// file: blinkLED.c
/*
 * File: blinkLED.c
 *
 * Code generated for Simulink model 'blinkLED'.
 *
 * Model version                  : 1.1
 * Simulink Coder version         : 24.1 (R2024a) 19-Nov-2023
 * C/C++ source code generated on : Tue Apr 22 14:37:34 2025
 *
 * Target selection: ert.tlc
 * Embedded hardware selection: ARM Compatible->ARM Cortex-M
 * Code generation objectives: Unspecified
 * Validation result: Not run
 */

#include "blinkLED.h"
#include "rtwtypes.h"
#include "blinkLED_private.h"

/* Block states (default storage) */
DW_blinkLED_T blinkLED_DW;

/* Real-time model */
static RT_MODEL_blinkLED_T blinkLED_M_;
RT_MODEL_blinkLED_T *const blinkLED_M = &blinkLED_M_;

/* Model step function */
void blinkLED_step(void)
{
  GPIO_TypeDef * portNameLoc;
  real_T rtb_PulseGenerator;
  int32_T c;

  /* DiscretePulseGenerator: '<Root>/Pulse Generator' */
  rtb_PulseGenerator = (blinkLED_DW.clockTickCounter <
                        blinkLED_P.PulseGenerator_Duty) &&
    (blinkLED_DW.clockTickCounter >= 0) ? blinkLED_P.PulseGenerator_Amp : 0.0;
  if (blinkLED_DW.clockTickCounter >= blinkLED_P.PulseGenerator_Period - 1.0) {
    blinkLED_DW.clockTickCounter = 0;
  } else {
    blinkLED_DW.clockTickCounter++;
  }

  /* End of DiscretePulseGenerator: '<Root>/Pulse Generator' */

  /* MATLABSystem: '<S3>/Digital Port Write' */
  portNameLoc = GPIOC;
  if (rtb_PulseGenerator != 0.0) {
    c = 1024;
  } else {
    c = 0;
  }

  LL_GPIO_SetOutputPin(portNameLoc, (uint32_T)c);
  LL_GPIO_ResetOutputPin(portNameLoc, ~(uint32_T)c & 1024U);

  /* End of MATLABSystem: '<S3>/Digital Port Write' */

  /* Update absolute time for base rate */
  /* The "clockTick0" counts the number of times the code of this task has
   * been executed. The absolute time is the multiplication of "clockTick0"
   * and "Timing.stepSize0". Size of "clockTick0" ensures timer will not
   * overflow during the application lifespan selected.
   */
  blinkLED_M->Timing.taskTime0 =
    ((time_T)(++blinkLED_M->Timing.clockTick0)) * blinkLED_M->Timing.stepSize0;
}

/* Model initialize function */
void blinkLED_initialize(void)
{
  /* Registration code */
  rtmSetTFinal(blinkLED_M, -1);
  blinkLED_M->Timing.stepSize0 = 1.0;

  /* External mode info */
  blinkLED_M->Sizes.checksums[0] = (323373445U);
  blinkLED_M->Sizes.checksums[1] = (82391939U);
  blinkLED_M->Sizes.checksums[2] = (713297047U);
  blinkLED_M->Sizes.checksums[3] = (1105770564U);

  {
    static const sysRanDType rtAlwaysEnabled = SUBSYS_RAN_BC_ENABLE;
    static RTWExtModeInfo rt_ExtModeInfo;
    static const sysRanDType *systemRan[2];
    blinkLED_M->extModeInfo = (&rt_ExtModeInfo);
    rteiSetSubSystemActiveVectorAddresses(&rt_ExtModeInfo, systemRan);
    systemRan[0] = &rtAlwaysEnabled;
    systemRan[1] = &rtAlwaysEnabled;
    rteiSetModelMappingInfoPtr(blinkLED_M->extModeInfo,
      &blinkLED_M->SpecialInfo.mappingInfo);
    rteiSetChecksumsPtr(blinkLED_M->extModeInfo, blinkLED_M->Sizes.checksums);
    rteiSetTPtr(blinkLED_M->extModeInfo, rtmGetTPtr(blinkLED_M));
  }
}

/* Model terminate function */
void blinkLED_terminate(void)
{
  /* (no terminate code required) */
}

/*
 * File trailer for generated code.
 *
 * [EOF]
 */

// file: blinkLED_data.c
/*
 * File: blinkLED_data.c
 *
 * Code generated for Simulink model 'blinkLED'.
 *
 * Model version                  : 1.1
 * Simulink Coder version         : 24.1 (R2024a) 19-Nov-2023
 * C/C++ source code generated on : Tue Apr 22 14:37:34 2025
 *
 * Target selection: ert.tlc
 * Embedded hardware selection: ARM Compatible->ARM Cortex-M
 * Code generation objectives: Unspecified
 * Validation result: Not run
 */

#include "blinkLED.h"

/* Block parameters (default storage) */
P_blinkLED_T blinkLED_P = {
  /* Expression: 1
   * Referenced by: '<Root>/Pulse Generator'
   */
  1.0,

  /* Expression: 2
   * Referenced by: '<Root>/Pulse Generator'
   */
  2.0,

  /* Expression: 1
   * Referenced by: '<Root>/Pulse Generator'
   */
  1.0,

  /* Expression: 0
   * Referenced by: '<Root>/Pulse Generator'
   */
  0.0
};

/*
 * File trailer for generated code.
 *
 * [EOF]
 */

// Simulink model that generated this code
simulink model "blinkLED"  (R2024a)
settings: Solver=FixedStepDiscrete  StartTime=0.0  StopTime=inf  FixedStep=1  RelTol=1e-3  EnableMultiTasking=on
libraries: stm32f4xxblockslib x1

== system blinkLED ==
  Digital Port Write : stm32f4xxblockslib/Digital Port Write  PortName=GPIOC  PinNumber=[10]  ReadOperation=off  IOAsArray=on  EnableSimPort=off  hoistedMaskSrc=ECSoC/ECSimCodegen/Digital Port Write
  Pulse Generator : DiscretePulseGenerator
  wires:
  Pulse Generator/1 -> Digital Port Write/1
